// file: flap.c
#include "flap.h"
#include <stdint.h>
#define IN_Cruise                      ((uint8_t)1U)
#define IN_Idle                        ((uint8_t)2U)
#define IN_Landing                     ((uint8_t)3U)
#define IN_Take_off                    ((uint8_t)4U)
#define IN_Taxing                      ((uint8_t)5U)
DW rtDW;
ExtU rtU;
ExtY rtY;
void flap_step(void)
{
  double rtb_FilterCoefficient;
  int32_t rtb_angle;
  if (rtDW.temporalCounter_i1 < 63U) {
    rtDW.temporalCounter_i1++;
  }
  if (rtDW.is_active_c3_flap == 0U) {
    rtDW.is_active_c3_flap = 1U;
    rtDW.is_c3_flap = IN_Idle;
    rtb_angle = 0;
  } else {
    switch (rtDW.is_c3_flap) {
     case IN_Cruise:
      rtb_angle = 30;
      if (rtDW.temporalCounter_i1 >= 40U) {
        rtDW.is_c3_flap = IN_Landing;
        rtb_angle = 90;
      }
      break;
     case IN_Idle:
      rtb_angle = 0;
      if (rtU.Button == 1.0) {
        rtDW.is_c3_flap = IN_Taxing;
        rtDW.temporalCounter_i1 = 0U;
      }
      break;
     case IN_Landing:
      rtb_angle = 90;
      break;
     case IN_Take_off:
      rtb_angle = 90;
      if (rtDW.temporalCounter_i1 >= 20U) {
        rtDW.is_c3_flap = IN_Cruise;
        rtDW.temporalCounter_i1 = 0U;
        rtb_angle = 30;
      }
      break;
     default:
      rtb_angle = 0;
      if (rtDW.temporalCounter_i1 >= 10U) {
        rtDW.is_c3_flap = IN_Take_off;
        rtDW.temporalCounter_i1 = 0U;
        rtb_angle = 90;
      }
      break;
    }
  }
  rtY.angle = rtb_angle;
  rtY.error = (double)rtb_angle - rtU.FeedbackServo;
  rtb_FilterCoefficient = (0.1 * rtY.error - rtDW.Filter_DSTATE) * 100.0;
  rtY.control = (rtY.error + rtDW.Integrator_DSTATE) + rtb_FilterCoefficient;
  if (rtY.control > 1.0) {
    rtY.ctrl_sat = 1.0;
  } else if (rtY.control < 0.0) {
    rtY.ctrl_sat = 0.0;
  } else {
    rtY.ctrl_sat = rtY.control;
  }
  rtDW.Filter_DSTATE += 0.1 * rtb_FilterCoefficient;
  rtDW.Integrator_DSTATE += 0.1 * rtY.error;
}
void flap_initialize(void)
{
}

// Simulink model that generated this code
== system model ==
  FeedbackServo : Inport
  Button : Inport
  angle : Outport  <- 1: Stateflowchart#1
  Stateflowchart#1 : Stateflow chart  <- 1: Button
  error : Outport  <- 1: Sum#1
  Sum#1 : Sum  Inputs=+-  <- 1: Stateflowchart#1, 2: FeedbackServo
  control : Outport  <- 1: PIDController#1
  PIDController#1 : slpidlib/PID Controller  Controller=PID  Form=Parallel  TimeDomain=Discrete-time  IntegratorMethod=Forward Euler  P=1  I=1  D=0.1  N=100  InitialConditionForIntegrator=0  ExternalReset=none  LimitOutput=off  UpperSaturationLimit=inf  LowerSaturationLimit=-inf  <- 1: Sum#1
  ctrl_sat : Outport  <- 1: Saturate#1
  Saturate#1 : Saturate  UpperLimit=1  LowerLimit=0  <- 1: PIDController#1
== stateflow chart Stateflowchart#1 ==
  state Taxing
    entry:
    angle=0;
  state Take_off
    entry:
    angle=90;
  state Cruise
    entry:
    angle=30;
  state Landing
    entry:
    angle=90;
  state Idle
    entry:
    angle=0;
  (default) -> (junction 31)
  Taxing -> Take_off : after(1,sec)
  Take_off -> Cruise : after(2,sec)
  Cruise -> Landing : after(4,sec)
  (junction 31) -> Idle
  Idle -> Taxing : [button==1]
  data: angle output; button input
